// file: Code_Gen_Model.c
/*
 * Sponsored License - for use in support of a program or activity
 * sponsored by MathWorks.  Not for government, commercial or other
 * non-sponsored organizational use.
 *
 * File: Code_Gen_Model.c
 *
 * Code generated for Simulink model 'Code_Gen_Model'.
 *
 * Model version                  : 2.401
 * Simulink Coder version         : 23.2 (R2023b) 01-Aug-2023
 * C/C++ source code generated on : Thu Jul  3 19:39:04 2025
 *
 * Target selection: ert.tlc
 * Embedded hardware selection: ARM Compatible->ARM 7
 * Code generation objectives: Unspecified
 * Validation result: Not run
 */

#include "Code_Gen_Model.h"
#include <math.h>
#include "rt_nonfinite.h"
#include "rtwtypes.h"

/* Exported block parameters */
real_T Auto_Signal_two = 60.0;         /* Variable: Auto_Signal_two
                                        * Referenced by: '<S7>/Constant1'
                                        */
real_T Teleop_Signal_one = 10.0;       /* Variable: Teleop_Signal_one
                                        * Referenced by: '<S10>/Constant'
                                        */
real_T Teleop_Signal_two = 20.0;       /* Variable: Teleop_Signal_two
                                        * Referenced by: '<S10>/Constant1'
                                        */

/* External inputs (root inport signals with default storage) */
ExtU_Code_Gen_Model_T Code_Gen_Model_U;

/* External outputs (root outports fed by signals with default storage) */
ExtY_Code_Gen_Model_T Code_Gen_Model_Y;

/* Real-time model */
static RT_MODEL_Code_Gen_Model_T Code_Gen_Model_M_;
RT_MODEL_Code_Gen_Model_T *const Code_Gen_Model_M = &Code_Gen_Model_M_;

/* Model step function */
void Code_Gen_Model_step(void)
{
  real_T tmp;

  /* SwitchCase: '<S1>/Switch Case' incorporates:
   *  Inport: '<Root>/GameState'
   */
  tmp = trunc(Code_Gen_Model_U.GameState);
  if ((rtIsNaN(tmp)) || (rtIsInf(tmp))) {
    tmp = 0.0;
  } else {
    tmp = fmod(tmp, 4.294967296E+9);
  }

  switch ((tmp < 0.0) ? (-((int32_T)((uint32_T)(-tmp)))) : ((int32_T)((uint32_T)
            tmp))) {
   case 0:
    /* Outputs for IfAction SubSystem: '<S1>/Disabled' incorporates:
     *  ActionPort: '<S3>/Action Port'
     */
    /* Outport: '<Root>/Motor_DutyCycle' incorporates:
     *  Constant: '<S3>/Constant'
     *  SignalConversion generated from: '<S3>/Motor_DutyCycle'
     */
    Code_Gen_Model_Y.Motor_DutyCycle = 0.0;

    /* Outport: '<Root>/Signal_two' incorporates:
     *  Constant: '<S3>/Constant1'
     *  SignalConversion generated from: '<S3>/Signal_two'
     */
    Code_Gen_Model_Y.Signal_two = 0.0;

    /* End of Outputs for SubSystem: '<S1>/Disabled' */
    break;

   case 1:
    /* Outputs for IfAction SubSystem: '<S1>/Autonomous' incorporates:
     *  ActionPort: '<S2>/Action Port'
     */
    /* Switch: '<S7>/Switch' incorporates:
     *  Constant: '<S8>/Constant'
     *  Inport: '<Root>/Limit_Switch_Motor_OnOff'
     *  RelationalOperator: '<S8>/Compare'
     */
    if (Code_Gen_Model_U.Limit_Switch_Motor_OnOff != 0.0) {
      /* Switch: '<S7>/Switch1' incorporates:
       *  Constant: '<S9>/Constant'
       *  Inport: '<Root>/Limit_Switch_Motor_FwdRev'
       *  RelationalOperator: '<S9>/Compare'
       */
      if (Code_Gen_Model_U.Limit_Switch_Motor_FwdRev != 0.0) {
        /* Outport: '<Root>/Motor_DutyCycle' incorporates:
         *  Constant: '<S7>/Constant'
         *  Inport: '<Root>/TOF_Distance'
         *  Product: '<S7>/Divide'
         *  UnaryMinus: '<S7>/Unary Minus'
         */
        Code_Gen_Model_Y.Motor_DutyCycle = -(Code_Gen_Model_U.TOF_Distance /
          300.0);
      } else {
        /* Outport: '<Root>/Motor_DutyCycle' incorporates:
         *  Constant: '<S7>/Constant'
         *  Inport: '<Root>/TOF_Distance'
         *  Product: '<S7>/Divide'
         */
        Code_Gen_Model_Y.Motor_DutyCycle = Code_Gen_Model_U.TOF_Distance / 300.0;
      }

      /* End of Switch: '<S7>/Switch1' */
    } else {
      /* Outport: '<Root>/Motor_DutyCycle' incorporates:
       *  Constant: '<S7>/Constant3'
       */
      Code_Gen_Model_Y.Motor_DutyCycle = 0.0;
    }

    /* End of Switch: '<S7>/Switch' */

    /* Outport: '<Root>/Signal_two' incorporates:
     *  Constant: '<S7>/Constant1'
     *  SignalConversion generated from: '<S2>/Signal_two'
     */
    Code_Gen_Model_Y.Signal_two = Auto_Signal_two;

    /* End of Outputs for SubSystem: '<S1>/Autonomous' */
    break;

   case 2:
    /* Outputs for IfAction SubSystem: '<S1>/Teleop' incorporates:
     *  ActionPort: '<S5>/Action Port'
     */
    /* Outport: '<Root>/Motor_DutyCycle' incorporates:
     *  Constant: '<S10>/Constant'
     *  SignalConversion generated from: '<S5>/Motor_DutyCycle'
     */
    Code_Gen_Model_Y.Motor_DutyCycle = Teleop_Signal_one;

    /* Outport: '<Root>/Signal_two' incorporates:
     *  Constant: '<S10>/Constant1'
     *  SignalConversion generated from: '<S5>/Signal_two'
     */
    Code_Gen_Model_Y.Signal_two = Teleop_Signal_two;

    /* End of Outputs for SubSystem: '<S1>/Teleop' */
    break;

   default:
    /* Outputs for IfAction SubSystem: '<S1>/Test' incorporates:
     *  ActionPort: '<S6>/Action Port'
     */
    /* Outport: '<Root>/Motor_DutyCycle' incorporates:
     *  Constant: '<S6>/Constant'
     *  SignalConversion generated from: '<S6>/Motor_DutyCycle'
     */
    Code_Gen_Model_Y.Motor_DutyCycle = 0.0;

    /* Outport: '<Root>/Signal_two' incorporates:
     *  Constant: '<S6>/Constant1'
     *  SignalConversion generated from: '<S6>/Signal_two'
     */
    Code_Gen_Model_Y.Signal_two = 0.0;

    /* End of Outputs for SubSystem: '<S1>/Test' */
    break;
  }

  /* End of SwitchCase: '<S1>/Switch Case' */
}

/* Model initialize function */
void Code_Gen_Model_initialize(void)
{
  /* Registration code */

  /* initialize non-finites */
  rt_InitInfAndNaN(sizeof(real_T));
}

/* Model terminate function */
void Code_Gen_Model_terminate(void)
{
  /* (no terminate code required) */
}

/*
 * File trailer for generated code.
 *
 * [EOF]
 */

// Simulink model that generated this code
simulink model "Code_Gen_Model"  (R2023b)
settings: Solver=FixedStepDiscrete  StartTime=0.0  StopTime=inf  FixedStep=t_sample  RelTol=1e-3

== system Code_Gen_Model ==
  GameState : Inport
  Limit_Switch_Motor_OnOff : Inport  Port=2
  Limit_Switch_Motor_FwdRev : Inport  Port=3
  TOF_Distance : Inport  Port=4
  RoboRio Controls : Subsystem  ReferencedSubsystem=RoboRio_Controls_sub
  Motor_DutyCycle : Outport
  Signal_two : Outport  Port=2
  wires:
  GameState/1 -> RoboRio Controls/1
  RoboRio Controls/1 -> Motor_DutyCycle/1
  RoboRio Controls/2 -> Signal_two/1
  Limit_Switch_Motor_OnOff/1 -> RoboRio Controls/2
  Limit_Switch_Motor_FwdRev/1 -> RoboRio Controls/3
  TOF_Distance/1 -> RoboRio Controls/4
